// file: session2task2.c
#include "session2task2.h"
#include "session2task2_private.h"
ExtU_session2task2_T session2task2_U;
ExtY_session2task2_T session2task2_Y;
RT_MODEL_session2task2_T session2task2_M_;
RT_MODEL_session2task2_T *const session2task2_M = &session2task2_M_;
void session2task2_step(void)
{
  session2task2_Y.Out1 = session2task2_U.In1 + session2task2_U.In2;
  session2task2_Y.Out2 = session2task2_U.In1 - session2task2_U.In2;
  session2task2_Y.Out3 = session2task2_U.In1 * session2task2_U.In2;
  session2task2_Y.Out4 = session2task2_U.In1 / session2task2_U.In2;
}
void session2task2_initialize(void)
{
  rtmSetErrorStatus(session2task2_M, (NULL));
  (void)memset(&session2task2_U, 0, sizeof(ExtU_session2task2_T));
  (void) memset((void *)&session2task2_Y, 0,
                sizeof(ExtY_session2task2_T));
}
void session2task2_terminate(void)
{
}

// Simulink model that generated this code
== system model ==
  In1 : Inport
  In2 : Inport
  Out1 : Outport  <- 1: Sum#1
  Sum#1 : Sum  <- 1: In1, 2: In2
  Out2 : Outport  <- 1: Sum#2
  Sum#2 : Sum  Inputs=+-  <- 1: In1, 2: In2
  Out3 : Outport  <- 1: Product#1
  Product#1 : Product  <- 1: In1, 2: In2
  Out4 : Outport  <- 1: Product#2
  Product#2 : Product  Inputs=*/  <- 1: In1, 2: In2
